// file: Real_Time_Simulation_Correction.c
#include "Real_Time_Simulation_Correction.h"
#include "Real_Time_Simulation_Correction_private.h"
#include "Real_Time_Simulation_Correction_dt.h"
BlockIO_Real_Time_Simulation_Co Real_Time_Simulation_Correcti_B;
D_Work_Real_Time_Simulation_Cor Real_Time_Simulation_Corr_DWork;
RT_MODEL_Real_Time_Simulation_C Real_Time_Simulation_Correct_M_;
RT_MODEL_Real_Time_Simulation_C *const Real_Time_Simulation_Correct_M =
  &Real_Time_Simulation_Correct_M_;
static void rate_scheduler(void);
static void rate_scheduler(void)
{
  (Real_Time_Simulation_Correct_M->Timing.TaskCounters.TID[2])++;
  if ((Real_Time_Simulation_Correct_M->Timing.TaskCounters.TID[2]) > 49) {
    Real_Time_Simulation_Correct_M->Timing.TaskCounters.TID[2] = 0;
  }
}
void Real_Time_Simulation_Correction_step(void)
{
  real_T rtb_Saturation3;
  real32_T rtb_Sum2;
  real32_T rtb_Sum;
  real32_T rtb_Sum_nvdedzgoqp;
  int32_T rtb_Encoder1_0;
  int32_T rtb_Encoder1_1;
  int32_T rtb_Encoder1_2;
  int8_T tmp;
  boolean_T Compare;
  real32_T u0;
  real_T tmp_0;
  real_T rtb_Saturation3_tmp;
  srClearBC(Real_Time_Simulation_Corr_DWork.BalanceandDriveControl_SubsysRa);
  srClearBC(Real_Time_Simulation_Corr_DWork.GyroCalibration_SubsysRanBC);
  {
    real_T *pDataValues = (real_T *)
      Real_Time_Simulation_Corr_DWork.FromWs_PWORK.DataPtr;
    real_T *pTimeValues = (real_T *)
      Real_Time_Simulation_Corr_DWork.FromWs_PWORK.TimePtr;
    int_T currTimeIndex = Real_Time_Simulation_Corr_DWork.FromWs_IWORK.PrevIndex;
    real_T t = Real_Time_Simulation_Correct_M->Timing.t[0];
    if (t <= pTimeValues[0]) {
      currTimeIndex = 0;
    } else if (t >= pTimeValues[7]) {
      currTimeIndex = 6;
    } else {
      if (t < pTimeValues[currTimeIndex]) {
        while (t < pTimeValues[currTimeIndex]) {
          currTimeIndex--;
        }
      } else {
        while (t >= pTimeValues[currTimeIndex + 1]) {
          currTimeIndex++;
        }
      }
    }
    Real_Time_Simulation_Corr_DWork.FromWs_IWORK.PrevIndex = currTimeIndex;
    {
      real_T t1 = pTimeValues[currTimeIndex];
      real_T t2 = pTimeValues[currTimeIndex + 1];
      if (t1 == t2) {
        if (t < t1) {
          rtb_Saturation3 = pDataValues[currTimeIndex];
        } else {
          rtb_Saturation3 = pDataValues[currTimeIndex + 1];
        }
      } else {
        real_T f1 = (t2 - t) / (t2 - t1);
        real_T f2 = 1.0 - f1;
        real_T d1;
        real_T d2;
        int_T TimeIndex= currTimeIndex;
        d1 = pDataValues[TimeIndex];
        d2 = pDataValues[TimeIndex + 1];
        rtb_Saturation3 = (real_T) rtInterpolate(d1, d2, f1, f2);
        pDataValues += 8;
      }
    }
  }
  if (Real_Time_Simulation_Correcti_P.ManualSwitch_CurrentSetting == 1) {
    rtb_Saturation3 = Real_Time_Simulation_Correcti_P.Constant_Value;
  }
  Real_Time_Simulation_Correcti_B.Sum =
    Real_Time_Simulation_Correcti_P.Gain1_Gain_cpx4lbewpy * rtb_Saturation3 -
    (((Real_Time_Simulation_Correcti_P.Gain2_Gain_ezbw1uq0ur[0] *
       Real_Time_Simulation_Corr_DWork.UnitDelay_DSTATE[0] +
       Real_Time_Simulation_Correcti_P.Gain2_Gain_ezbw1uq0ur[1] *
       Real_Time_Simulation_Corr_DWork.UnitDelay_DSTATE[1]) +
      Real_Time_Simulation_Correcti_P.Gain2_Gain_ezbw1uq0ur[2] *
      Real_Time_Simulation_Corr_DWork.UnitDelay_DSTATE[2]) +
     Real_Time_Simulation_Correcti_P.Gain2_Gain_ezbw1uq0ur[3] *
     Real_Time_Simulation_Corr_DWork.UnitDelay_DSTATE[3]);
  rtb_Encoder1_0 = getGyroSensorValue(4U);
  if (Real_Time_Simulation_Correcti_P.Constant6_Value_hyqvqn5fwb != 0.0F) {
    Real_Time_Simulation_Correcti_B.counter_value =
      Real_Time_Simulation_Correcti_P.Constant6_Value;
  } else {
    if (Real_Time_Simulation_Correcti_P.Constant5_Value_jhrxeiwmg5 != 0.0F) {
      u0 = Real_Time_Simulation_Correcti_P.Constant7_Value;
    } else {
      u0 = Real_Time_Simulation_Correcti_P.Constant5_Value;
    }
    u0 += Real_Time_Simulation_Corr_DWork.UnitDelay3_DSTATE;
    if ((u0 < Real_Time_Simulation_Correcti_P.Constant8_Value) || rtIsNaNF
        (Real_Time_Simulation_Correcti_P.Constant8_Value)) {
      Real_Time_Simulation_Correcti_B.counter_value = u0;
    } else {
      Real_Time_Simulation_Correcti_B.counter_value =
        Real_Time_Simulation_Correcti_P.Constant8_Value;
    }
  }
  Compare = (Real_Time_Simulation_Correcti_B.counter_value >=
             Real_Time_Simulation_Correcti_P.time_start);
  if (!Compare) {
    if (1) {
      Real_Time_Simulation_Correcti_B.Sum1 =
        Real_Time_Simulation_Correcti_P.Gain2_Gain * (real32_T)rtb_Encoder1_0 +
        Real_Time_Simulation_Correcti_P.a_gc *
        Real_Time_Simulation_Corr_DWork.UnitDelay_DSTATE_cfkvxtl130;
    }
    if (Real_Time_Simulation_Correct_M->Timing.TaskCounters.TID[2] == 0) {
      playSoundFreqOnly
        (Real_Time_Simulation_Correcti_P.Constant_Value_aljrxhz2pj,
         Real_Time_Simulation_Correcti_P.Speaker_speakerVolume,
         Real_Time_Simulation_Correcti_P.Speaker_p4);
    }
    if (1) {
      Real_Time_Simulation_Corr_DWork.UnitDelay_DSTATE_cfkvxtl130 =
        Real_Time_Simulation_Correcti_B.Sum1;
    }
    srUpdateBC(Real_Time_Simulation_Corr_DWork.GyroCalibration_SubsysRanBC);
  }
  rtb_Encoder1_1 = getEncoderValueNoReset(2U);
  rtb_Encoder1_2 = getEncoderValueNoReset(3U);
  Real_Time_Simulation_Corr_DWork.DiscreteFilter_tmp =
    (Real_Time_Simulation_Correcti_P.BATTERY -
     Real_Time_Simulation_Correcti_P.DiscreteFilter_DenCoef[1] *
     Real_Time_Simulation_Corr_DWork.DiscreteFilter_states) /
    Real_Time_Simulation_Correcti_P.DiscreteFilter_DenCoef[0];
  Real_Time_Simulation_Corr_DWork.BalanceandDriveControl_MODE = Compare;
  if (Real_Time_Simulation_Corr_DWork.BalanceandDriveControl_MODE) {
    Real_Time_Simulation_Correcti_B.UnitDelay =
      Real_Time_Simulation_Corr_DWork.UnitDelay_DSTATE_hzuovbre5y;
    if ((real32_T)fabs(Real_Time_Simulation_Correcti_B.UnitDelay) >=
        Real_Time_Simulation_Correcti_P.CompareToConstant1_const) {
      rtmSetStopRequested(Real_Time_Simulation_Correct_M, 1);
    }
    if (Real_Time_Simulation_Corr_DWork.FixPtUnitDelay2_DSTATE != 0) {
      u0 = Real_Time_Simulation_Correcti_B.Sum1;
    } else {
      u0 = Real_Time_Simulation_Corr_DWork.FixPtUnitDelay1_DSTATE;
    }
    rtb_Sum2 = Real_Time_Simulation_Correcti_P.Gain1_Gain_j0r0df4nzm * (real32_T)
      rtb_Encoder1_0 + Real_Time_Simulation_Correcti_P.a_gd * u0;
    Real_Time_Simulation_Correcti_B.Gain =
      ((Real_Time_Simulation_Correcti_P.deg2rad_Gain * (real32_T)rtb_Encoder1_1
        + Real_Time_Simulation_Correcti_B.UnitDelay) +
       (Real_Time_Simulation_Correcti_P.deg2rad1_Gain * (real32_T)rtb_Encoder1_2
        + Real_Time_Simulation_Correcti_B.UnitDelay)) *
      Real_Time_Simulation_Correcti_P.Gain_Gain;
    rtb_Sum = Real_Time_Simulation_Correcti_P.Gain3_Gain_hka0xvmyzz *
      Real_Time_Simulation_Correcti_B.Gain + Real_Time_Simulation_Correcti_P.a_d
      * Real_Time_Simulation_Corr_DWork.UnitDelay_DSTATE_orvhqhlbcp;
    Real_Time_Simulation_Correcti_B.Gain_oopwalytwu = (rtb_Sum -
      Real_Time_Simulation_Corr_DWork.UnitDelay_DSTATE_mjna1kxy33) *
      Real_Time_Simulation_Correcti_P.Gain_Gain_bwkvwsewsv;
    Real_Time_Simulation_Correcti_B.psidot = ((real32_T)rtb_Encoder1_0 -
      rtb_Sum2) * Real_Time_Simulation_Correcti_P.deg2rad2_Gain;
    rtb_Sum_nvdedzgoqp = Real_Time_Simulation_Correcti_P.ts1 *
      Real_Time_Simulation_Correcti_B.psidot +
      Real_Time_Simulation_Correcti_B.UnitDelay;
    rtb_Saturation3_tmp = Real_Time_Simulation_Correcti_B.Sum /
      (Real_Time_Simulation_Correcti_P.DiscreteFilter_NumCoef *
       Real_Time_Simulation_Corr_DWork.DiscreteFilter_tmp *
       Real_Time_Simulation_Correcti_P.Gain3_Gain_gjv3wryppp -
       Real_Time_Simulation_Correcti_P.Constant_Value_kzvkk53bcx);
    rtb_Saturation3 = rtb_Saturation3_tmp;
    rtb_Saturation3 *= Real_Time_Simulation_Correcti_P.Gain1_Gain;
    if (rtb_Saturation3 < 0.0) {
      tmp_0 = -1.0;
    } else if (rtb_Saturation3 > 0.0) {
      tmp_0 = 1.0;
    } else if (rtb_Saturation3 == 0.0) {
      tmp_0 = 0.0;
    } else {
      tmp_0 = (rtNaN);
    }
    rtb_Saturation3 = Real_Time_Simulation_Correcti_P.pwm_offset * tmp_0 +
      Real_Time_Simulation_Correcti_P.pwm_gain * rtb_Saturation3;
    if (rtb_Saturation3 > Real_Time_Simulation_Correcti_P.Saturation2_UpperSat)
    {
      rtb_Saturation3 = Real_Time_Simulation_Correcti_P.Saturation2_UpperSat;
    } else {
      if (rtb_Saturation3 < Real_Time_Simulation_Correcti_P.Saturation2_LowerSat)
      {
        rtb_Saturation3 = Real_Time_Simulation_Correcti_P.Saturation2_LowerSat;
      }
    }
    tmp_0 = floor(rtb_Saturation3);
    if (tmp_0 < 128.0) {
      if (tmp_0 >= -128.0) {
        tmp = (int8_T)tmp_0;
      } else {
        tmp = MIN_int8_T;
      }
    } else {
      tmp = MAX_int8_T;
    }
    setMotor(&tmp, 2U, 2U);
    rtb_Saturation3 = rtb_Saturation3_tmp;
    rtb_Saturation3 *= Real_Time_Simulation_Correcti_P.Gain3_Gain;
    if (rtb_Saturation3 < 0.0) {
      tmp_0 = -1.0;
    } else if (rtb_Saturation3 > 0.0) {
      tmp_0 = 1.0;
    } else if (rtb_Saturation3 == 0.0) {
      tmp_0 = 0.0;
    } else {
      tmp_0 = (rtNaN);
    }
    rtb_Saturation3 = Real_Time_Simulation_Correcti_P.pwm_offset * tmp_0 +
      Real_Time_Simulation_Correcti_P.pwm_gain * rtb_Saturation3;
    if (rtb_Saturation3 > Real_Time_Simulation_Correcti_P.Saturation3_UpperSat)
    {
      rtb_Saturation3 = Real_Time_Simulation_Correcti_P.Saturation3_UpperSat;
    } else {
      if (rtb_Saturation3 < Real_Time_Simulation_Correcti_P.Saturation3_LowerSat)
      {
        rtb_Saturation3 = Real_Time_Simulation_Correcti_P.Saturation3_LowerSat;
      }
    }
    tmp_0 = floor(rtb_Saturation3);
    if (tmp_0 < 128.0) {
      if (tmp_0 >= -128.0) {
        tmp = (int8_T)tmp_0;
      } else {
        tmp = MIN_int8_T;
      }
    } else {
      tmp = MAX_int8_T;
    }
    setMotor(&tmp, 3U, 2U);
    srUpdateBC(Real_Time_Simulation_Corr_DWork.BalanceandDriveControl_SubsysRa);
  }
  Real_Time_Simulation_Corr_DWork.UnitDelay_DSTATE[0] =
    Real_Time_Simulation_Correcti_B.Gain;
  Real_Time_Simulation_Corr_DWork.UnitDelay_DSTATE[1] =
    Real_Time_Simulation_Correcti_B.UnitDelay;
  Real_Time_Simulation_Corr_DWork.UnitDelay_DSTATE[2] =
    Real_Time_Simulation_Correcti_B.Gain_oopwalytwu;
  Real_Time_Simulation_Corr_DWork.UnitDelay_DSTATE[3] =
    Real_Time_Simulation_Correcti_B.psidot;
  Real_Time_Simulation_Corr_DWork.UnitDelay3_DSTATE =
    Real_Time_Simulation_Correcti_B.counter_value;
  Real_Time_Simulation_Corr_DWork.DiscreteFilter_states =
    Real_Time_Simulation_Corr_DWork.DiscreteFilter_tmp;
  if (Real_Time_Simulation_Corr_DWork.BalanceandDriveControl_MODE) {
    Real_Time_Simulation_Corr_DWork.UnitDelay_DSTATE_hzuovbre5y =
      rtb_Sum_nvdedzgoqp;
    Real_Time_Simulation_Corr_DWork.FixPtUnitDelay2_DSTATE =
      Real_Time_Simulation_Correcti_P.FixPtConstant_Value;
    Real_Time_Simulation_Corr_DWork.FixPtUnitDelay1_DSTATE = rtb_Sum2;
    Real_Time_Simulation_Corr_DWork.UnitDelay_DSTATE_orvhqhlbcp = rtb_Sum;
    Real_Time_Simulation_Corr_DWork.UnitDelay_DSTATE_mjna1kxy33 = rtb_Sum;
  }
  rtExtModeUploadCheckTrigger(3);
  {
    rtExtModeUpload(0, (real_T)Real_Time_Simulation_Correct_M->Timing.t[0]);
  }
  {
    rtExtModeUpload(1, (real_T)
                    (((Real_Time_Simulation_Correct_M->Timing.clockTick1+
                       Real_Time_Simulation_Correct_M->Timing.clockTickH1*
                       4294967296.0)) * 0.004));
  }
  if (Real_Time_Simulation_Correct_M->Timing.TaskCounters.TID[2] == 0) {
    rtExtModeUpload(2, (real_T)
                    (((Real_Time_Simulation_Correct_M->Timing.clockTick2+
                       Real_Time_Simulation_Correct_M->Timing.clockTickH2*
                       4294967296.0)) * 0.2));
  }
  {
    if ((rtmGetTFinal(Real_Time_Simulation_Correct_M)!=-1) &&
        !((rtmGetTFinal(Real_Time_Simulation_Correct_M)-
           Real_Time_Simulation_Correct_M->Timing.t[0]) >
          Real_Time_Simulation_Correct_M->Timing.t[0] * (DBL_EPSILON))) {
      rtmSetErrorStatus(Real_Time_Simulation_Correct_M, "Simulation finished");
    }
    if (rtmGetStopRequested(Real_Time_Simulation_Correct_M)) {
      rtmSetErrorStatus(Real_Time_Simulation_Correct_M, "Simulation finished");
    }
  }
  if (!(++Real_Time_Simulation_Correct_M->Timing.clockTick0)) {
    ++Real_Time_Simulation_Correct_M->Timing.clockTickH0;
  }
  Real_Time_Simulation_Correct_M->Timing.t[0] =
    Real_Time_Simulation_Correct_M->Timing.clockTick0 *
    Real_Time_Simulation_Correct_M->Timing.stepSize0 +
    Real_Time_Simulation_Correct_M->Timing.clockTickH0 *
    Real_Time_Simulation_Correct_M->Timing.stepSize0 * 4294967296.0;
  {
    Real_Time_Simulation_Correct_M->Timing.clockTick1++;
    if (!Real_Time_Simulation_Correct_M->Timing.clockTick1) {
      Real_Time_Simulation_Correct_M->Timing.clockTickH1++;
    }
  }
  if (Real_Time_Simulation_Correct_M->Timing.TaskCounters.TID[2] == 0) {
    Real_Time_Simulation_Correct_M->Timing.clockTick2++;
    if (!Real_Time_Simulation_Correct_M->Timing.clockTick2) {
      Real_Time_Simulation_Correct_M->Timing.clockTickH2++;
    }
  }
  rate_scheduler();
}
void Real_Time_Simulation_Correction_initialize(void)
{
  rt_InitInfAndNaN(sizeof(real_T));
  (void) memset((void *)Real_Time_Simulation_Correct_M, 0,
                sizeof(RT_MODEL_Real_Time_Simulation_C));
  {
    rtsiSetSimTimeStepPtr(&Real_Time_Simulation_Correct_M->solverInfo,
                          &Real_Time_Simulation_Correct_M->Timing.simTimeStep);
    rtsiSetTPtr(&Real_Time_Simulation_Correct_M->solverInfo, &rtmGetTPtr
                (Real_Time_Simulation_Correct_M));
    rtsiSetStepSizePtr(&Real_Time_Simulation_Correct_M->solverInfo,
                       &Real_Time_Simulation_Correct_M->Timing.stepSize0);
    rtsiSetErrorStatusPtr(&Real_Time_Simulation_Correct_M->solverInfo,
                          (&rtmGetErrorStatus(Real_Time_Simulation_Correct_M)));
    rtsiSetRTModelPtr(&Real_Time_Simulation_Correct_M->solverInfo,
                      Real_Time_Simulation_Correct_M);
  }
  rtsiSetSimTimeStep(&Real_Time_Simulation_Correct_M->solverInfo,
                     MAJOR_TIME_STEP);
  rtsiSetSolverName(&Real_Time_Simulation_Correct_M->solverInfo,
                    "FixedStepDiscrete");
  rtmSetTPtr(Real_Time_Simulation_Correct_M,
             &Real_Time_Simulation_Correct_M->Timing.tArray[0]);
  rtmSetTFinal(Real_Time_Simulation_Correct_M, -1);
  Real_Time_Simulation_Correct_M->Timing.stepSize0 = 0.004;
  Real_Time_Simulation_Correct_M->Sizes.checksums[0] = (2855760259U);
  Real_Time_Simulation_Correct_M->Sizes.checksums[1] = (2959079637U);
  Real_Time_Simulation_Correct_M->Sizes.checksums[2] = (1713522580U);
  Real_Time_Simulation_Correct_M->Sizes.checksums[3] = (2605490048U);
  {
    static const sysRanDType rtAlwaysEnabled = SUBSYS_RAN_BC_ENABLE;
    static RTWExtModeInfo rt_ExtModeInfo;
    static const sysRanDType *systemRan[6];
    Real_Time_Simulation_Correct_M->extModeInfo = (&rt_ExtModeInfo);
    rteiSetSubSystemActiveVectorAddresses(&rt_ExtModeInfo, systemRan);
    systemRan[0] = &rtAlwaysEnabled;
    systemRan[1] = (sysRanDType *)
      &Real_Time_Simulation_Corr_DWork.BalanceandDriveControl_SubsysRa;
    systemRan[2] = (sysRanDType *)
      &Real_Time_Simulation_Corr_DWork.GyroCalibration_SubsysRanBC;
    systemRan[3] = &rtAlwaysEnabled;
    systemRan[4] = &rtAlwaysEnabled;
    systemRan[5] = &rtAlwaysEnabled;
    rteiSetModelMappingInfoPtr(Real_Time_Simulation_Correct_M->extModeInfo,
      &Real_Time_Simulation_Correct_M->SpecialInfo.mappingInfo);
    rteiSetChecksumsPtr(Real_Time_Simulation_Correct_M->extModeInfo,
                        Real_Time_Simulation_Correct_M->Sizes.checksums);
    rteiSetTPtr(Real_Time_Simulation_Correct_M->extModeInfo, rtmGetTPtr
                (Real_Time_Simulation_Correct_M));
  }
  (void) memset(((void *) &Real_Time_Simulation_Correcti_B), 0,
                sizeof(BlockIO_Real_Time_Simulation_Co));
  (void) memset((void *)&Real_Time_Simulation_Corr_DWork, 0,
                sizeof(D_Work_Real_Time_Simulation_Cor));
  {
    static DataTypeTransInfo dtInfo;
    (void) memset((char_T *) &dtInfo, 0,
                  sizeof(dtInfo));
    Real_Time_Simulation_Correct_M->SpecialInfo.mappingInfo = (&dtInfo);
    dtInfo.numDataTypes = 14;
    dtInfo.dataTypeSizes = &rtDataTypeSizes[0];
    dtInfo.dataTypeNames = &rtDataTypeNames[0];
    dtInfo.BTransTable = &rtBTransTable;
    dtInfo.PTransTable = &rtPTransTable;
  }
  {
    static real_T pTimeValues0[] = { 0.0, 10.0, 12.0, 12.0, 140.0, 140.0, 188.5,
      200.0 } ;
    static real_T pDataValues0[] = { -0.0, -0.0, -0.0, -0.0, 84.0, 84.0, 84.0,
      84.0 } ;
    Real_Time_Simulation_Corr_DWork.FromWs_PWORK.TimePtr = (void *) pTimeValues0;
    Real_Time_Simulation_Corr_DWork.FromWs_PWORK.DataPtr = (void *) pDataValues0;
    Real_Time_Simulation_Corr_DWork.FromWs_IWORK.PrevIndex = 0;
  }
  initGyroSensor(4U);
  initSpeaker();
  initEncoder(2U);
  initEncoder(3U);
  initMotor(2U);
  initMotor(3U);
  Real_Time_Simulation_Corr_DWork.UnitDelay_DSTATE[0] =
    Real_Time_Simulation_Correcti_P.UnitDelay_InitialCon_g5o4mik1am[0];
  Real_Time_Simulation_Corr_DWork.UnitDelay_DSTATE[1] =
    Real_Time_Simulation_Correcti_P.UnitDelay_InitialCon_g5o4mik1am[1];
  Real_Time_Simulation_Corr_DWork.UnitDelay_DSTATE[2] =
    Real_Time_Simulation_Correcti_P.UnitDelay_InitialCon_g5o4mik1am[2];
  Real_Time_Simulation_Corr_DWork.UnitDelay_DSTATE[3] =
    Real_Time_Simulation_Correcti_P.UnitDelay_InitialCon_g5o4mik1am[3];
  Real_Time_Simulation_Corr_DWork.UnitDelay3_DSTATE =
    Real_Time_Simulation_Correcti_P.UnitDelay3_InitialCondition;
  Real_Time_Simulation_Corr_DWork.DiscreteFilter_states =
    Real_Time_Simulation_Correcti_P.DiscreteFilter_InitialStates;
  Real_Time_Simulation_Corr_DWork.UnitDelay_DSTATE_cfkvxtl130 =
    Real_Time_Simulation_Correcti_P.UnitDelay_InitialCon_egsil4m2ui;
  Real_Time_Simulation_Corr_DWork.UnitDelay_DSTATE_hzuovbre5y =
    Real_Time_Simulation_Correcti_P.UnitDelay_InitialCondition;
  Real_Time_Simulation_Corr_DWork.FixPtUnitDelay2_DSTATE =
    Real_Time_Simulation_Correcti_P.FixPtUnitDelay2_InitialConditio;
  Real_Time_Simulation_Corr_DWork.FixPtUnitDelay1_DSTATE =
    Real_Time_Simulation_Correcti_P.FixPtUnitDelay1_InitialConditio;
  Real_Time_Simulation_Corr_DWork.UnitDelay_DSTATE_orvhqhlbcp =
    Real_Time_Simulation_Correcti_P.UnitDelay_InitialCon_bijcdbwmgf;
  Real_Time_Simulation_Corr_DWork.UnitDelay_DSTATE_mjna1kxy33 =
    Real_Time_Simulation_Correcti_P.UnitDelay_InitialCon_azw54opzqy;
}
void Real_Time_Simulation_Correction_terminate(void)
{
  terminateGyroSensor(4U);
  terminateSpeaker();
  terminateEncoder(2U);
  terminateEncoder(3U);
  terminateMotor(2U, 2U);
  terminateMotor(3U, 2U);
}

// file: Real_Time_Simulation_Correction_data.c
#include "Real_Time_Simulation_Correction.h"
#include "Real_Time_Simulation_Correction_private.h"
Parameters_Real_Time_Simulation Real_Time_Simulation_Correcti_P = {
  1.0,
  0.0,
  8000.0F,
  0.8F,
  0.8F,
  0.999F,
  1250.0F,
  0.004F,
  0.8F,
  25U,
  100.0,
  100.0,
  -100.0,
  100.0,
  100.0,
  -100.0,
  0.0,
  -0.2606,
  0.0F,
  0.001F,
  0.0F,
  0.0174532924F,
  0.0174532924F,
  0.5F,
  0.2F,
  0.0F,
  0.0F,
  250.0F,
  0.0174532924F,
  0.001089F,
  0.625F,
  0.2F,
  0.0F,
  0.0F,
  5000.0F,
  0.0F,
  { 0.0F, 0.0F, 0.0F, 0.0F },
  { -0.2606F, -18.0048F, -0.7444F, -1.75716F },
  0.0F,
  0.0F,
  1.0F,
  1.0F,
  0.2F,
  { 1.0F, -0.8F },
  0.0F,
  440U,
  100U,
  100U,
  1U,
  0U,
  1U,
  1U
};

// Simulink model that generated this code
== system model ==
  Sum1 : Sum  Inputs=+-  <- 1: Constant8, 2: Switch#1
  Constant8 : Constant  Value=5000
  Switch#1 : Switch  Criteria=u2 ~= 0  <- 1: Constant6, 2: Constant#1, 3: MinMax#1
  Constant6 : Constant  Value=0
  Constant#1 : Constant  Value=0
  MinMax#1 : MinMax  Inputs=2  <- 1: Sum, 2: Constant8
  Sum : Sum  <- 1: UnitDelay3, 2: Switch#2
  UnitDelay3 : UnitDelay  <- 1: Switch#1
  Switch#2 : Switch  Criteria=u2 ~= 0  <- 1: Constant7, 2: Constant5, 3: Constant#2
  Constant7 : Constant
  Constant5 : Constant
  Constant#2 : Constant  Value=0
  FromWs : FromWorkspace
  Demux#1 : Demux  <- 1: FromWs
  ManualSwitch : ManualSwitch  <- 1: Constant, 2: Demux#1
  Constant : Constant  Value=0
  Sum#1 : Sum  Inputs=+-  <- 1: Gain1, 2: Gain2
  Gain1 : Gain  Gain=-0.2606  <- 1: ManualSwitch
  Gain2 : Gain  Gain="[-0.2606 -18.0048  -0.7444 -1.75716]"  Multiplication=Matrix(K*u)  <- 1: UnitDelay
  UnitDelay : UnitDelay  InitialCondition=[0; 0; 0; 0]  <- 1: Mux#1
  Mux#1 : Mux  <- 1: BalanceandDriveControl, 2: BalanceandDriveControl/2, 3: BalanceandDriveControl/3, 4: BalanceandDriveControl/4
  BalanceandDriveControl : Subsystem  <- 1: GyroCalibration, 2: DataTypeConversion#1, 3: DataTypeConversion#2, 4: DataTypeConversion#3, 5: DiscreteFilter, 6: Sum#1, 7: Sum#1, Enable: CompareToConstant#1
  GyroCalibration : Subsystem  <- 1: DataTypeConversion#1, Enable: Logic#1
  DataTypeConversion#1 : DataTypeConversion  <- 1: GyroSensor#1
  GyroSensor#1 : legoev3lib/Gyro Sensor
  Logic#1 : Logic  Operator=NOT  <- 1: CompareToConstant#1
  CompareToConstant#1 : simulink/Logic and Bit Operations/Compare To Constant  relop=>=  const=time_start  <- 1: DataTypeConversion#4
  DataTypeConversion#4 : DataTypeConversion  <- 1: Switch#1
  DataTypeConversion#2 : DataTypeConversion  <- 1: Encoder#1
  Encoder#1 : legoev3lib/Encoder
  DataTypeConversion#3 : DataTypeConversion  <- 1: Encoder1
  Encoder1 : legoev3lib/Encoder
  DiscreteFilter : DiscreteFilter  Numerator=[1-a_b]  Denominator=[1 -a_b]  <- 1: DataTypeConversion#5
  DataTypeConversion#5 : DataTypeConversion  <- 1: Constant#3
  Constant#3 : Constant  Value=BATTERY
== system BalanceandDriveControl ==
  Inport#1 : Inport
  Inport#2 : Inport
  Inport#3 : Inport
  Inport#4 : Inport
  Inport#5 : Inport
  Inport#6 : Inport
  Inport#7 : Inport
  EnablePort#1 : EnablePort
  Outport#1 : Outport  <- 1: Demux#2
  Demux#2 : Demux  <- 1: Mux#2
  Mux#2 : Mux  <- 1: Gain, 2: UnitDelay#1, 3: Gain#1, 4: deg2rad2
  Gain : Gain  Gain=1/2  <- 1: Sum#2
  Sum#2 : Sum  Inputs=++  <- 1: Sum#3, 2: Sum#4
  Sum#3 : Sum  Inputs=++  <- 1: deg2rad, 2: UnitDelay#1
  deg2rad : Gain  Gain=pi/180  <- 1: Inport#3
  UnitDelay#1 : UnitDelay  <- 1: Sum#5
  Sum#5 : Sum  Inputs=++  <- 1: Gain#2, 2: UnitDelay#1
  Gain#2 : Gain  Gain=ts1  <- 1: deg2rad2
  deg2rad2 : Gain  Gain=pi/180  <- 1: Sum2
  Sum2 : Sum  Inputs=+-  <- 1: Inport#2, 2: Sum#6
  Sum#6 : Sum  Inputs=++  <- 1: Gain#3, 2: Gain#4
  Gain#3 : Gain  Gain=1-a_gd  <- 1: Inport#2
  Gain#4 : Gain  Gain=a_gd  <- 1: UnitDelayExternalIC#1
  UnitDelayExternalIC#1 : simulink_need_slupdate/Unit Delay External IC  <- 1: Sum#6, 2: Inport#1
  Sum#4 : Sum  Inputs=++  <- 1: deg2rad1, 2: UnitDelay#1
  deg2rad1 : Gain  Gain=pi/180  <- 1: Inport#4
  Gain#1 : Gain  Gain=1/ts1  <- 1: Sum#7
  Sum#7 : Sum  Inputs=+-  <- 1: Sum#8, 2: UnitDelay#2
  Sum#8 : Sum  Inputs=++  <- 1: Gain3, 2: Gain#5
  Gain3 : Gain  Gain=1-a_d  <- 1: Gain
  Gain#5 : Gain  Gain=a_d  <- 1: UnitDelay#3
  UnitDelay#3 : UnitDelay  <- 1: Sum#8
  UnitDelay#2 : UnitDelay  <- 1: Sum#8
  Outport#2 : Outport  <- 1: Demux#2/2
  Outport#3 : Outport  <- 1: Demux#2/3
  Outport#4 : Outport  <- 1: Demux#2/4
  Stop#1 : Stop  <- 1: CompareToConstant1
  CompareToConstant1 : simulink/Logic and Bit Operations/Compare To Constant  relop=>=  const=0.8  <- 1: Abs#1
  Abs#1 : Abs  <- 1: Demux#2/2
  Motor#1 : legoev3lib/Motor  <- 1: Saturation2
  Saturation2 : Saturate  UpperLimit=100  LowerLimit=-100  <- 1: CoulombViscousFriction#1
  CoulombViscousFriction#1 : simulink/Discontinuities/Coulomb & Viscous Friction  <- 1: Gain#6
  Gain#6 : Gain  Gain=100  <- 1: Product#1
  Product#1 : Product  Inputs=*/  <- 1: Inport#6, 2: Sum#9
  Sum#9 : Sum  Inputs=+-  <- 1: Gain#7, 2: Constant#4
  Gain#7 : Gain  Gain=0.001089  <- 1: Inport#5
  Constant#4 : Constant  Value=0.625
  Motor#2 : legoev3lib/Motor  <- 1: Saturation3
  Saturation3 : Saturate  UpperLimit=100  LowerLimit=-100  <- 1: CoulombViscousFriction#2
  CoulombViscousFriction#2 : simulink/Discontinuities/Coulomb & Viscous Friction  <- 1: Gain#8
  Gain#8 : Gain  Gain=100  <- 1: Product#2
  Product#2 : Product  Inputs=*/  <- 1: Inport#7, 2: Sum#9
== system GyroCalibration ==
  Inport#8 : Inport
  EnablePort#2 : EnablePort
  Outport#5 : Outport  <- 1: Sum#10
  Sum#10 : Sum  Inputs=++  <- 1: Gain#9, 2: Gain#10
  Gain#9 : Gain  Gain=1-a_gc  <- 1: Inport#8
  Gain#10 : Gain  Gain=a_gc  <- 1: UnitDelay#4
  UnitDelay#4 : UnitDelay  <- 1: Sum#10
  Speaker#1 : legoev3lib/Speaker  <- 1: Constant#5
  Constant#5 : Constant  Value=440
